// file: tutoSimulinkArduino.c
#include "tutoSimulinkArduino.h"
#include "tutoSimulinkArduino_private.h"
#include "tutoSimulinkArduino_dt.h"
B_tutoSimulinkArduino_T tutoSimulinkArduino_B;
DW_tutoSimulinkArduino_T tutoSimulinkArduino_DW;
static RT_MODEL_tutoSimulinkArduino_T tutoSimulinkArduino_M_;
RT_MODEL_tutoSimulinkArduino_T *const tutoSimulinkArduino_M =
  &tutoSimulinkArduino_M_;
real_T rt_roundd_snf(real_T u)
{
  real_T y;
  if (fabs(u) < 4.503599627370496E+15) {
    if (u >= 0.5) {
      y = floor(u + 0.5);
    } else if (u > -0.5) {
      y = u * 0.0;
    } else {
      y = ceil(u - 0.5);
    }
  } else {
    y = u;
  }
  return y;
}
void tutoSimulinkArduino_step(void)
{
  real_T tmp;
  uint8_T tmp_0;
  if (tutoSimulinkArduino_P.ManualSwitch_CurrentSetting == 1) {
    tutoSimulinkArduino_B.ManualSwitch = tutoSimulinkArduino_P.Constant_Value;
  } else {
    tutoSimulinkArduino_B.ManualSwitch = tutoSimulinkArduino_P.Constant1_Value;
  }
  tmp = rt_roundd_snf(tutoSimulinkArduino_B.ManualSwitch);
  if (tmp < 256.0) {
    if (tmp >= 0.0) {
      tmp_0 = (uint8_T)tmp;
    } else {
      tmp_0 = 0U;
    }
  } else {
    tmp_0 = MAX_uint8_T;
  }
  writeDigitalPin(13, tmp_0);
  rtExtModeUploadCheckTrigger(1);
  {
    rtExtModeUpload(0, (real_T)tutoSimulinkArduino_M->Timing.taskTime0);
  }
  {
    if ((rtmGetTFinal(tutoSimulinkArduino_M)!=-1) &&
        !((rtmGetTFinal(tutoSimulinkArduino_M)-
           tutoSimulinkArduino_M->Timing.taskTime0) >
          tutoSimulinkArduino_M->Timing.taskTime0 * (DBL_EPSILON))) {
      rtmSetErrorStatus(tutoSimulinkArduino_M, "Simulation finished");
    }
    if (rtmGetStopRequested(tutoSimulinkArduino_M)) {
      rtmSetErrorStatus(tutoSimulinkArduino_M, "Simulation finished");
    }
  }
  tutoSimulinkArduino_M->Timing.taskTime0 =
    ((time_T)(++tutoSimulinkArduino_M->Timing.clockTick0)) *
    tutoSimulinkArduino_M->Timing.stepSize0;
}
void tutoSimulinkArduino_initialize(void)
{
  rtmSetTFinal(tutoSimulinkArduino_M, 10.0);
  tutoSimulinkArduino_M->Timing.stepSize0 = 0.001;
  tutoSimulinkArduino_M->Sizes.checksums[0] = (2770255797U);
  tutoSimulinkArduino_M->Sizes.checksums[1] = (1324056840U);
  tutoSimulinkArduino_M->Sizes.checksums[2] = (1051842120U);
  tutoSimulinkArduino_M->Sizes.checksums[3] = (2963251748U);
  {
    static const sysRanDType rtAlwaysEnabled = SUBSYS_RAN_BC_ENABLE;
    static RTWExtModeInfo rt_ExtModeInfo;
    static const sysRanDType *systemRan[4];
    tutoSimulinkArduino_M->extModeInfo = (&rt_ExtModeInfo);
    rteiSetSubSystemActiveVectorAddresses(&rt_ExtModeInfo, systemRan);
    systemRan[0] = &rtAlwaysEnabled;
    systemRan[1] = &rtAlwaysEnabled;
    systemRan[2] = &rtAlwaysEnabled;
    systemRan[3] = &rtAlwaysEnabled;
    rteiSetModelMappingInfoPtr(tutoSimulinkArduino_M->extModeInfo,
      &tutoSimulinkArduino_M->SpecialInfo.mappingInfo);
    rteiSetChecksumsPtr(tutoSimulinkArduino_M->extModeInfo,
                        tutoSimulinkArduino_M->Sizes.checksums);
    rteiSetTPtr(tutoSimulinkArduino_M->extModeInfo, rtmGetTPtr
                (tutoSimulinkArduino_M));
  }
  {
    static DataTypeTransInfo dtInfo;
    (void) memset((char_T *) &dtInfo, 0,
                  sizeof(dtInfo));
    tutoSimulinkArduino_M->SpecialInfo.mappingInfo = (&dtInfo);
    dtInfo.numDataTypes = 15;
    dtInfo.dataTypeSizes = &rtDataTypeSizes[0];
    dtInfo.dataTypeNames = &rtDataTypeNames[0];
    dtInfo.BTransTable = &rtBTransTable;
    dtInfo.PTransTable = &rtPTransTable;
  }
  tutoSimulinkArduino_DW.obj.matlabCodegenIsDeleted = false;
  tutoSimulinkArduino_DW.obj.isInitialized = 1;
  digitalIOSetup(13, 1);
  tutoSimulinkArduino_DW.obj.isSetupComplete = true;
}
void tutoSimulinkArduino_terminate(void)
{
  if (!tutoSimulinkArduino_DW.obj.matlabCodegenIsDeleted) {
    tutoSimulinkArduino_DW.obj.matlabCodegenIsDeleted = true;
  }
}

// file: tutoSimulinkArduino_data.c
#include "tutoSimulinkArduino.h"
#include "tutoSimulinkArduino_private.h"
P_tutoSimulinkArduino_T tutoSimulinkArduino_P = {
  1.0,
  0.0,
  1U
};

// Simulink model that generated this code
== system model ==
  WiFiUDPSend#1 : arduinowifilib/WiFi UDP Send  <- 1: Constant
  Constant : Constant
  DigitalOutput#1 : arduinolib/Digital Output  pinNumber=13  <- 1: ManualSwitch
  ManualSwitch : ManualSwitch  <- 1: Constant, 2: Constant1
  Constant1 : Constant  Value=0
